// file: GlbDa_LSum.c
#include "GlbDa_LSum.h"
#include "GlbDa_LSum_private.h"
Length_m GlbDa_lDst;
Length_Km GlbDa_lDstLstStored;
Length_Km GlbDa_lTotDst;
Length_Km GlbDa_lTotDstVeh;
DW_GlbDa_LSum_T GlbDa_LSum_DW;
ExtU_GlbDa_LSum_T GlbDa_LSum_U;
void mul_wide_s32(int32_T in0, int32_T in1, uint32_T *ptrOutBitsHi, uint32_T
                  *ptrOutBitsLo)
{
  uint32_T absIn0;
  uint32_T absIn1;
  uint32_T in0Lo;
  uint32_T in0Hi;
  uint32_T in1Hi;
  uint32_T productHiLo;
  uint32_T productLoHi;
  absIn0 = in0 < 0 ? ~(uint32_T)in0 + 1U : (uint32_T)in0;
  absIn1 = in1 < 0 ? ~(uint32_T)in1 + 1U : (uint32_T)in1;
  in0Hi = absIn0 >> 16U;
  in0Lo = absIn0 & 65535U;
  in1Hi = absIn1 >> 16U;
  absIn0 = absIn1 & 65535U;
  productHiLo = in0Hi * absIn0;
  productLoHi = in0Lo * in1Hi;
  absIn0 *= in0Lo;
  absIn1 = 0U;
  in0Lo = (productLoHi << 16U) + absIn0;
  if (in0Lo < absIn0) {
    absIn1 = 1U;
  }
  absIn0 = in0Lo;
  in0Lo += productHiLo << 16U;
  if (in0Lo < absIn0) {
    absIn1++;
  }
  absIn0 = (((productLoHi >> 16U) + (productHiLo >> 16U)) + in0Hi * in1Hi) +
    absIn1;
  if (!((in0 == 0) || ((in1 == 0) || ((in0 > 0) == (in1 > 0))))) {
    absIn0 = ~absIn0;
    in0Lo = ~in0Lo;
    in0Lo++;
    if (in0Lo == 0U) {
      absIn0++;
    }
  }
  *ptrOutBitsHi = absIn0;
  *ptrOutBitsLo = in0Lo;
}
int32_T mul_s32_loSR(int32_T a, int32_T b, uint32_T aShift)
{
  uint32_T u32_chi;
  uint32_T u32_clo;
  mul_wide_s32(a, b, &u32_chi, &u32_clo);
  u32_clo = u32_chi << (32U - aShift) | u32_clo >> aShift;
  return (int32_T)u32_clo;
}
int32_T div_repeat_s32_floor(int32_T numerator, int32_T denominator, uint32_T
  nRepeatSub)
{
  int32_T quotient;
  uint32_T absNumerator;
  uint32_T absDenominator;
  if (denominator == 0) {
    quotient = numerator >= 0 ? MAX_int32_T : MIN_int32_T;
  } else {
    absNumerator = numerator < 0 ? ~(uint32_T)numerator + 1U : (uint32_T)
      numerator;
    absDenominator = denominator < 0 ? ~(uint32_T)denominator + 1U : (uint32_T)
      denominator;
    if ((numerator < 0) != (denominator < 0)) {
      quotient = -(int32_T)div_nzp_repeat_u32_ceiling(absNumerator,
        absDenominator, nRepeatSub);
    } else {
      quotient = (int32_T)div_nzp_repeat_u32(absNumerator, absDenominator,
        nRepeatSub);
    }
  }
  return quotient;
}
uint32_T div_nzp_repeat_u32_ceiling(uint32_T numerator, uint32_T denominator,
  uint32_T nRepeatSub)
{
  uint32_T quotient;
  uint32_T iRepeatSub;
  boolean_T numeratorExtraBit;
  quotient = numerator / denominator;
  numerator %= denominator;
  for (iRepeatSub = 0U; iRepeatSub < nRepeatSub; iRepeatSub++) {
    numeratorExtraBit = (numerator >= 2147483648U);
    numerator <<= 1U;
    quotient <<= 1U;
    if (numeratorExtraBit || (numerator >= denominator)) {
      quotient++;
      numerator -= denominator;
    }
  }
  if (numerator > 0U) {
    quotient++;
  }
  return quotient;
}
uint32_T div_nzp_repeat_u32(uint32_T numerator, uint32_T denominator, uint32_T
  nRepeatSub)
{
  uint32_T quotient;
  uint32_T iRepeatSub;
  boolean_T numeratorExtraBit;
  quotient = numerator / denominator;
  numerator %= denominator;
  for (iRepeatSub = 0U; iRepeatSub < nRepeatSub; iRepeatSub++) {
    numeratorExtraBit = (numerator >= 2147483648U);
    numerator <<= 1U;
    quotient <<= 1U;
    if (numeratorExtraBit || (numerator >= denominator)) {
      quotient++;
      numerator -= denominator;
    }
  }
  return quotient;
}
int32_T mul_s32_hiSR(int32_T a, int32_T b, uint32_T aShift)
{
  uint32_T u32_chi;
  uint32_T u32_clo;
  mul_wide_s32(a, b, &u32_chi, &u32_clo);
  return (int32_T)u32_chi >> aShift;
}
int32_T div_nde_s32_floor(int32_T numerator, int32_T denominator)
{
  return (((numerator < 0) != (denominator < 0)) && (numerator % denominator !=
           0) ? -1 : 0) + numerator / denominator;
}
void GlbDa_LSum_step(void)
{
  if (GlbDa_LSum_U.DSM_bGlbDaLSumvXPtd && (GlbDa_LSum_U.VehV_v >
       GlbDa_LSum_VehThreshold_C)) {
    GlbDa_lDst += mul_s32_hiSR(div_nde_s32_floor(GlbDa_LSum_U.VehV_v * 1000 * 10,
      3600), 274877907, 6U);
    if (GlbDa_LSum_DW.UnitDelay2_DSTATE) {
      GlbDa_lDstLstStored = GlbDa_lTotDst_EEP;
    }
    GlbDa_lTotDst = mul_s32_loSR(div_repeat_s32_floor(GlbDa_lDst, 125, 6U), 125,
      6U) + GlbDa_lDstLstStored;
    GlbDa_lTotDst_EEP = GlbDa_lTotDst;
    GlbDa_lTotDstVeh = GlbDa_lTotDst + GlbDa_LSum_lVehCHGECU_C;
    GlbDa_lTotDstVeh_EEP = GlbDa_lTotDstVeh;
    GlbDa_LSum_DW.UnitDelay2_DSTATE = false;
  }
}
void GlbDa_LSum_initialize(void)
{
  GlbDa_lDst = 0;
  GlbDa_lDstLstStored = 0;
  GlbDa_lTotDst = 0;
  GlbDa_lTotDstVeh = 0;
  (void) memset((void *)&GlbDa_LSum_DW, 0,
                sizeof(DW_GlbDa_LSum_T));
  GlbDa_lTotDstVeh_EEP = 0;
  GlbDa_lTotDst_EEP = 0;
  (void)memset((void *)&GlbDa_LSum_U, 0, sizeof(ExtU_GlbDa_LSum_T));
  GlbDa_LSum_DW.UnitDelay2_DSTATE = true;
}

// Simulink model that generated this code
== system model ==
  VehV_v : Inport
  DSM_bGlbDaLSumvXPtd : Inport
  TriggerPort#1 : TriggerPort  TriggerType=function-call
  GlbDa_lTotDst : Outport  <- 1: Subsystem#1
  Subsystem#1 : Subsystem  <- 1: VehV_v, Enable: Logic#1
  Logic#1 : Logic  <- 1: DSM_bGlbDaLSumvXPtd, 2: RelationalOperator#1
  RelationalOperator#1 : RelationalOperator  Operator=>  <- 1: VehV_v, 2: Constant#1
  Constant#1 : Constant  Value=GlbDa_LSum_VehThreshold_C
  GlbDa_lDstLstStored : Outport  <- 1: Subsystem#1/2
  GlbDa_lTotDstVeh : Outport  <- 1: Subsystem#1/3
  GlbDa_lDst : Outport  <- 1: Subsystem#1/4
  DataStoreMemory#1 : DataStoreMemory  DataStoreName=GlbDa_lTotDstVeh_EEP
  DataStoreMemory#2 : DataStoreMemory  DataStoreName=GlbDa_lTotDst_EEP
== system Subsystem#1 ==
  Inport#1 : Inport
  EnablePort#1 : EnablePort
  Outport#1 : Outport  <- 1: Sum#1
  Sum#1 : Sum  <- 1: Product#1, 2: Switch#1
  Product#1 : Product  Inputs=*/  <- 1: Sum#2, 2: Constant#2
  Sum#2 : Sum  <- 1: Product#2, 2: UnitDelay#1
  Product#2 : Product  Inputs=*/  <- 1: Product#3, 2: Constant#3
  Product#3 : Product  <- 1: Inport#1, 2: Constant#4
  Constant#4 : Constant  Value=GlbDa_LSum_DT
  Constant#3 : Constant  Value=3600
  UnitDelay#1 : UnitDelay  <- 1: Sum#2
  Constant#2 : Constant  Value=1000
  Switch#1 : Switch  Criteria=u2 ~= 0  <- 1: DataStoreRead#1, 2: UnitDelay2, 3: UnitDelay#2
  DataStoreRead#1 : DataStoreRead  DataStoreName=GlbDa_lTotDst_EEP
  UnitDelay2 : UnitDelay  InitialCondition=true  <- 1: Constant#5
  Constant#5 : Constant  Value=0
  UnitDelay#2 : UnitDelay  <- 1: Switch#1
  Outport#2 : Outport  <- 1: Switch#1
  Outport#3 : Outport  <- 1: Sum#3
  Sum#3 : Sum  <- 1: Sum#1, 2: Constant#6
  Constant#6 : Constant  Value=GlbDa_LSum_lVehCHGECU_C
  Outport#4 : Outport  <- 1: Sum#2
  DataStoreWrite#1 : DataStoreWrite  DataStoreName=GlbDa_lTotDst_EEP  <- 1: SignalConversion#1
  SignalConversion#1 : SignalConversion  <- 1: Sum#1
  DataStoreWrite#2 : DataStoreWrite  DataStoreName=GlbDa_lTotDstVeh_EEP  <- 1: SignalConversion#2
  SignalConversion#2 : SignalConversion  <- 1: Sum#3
